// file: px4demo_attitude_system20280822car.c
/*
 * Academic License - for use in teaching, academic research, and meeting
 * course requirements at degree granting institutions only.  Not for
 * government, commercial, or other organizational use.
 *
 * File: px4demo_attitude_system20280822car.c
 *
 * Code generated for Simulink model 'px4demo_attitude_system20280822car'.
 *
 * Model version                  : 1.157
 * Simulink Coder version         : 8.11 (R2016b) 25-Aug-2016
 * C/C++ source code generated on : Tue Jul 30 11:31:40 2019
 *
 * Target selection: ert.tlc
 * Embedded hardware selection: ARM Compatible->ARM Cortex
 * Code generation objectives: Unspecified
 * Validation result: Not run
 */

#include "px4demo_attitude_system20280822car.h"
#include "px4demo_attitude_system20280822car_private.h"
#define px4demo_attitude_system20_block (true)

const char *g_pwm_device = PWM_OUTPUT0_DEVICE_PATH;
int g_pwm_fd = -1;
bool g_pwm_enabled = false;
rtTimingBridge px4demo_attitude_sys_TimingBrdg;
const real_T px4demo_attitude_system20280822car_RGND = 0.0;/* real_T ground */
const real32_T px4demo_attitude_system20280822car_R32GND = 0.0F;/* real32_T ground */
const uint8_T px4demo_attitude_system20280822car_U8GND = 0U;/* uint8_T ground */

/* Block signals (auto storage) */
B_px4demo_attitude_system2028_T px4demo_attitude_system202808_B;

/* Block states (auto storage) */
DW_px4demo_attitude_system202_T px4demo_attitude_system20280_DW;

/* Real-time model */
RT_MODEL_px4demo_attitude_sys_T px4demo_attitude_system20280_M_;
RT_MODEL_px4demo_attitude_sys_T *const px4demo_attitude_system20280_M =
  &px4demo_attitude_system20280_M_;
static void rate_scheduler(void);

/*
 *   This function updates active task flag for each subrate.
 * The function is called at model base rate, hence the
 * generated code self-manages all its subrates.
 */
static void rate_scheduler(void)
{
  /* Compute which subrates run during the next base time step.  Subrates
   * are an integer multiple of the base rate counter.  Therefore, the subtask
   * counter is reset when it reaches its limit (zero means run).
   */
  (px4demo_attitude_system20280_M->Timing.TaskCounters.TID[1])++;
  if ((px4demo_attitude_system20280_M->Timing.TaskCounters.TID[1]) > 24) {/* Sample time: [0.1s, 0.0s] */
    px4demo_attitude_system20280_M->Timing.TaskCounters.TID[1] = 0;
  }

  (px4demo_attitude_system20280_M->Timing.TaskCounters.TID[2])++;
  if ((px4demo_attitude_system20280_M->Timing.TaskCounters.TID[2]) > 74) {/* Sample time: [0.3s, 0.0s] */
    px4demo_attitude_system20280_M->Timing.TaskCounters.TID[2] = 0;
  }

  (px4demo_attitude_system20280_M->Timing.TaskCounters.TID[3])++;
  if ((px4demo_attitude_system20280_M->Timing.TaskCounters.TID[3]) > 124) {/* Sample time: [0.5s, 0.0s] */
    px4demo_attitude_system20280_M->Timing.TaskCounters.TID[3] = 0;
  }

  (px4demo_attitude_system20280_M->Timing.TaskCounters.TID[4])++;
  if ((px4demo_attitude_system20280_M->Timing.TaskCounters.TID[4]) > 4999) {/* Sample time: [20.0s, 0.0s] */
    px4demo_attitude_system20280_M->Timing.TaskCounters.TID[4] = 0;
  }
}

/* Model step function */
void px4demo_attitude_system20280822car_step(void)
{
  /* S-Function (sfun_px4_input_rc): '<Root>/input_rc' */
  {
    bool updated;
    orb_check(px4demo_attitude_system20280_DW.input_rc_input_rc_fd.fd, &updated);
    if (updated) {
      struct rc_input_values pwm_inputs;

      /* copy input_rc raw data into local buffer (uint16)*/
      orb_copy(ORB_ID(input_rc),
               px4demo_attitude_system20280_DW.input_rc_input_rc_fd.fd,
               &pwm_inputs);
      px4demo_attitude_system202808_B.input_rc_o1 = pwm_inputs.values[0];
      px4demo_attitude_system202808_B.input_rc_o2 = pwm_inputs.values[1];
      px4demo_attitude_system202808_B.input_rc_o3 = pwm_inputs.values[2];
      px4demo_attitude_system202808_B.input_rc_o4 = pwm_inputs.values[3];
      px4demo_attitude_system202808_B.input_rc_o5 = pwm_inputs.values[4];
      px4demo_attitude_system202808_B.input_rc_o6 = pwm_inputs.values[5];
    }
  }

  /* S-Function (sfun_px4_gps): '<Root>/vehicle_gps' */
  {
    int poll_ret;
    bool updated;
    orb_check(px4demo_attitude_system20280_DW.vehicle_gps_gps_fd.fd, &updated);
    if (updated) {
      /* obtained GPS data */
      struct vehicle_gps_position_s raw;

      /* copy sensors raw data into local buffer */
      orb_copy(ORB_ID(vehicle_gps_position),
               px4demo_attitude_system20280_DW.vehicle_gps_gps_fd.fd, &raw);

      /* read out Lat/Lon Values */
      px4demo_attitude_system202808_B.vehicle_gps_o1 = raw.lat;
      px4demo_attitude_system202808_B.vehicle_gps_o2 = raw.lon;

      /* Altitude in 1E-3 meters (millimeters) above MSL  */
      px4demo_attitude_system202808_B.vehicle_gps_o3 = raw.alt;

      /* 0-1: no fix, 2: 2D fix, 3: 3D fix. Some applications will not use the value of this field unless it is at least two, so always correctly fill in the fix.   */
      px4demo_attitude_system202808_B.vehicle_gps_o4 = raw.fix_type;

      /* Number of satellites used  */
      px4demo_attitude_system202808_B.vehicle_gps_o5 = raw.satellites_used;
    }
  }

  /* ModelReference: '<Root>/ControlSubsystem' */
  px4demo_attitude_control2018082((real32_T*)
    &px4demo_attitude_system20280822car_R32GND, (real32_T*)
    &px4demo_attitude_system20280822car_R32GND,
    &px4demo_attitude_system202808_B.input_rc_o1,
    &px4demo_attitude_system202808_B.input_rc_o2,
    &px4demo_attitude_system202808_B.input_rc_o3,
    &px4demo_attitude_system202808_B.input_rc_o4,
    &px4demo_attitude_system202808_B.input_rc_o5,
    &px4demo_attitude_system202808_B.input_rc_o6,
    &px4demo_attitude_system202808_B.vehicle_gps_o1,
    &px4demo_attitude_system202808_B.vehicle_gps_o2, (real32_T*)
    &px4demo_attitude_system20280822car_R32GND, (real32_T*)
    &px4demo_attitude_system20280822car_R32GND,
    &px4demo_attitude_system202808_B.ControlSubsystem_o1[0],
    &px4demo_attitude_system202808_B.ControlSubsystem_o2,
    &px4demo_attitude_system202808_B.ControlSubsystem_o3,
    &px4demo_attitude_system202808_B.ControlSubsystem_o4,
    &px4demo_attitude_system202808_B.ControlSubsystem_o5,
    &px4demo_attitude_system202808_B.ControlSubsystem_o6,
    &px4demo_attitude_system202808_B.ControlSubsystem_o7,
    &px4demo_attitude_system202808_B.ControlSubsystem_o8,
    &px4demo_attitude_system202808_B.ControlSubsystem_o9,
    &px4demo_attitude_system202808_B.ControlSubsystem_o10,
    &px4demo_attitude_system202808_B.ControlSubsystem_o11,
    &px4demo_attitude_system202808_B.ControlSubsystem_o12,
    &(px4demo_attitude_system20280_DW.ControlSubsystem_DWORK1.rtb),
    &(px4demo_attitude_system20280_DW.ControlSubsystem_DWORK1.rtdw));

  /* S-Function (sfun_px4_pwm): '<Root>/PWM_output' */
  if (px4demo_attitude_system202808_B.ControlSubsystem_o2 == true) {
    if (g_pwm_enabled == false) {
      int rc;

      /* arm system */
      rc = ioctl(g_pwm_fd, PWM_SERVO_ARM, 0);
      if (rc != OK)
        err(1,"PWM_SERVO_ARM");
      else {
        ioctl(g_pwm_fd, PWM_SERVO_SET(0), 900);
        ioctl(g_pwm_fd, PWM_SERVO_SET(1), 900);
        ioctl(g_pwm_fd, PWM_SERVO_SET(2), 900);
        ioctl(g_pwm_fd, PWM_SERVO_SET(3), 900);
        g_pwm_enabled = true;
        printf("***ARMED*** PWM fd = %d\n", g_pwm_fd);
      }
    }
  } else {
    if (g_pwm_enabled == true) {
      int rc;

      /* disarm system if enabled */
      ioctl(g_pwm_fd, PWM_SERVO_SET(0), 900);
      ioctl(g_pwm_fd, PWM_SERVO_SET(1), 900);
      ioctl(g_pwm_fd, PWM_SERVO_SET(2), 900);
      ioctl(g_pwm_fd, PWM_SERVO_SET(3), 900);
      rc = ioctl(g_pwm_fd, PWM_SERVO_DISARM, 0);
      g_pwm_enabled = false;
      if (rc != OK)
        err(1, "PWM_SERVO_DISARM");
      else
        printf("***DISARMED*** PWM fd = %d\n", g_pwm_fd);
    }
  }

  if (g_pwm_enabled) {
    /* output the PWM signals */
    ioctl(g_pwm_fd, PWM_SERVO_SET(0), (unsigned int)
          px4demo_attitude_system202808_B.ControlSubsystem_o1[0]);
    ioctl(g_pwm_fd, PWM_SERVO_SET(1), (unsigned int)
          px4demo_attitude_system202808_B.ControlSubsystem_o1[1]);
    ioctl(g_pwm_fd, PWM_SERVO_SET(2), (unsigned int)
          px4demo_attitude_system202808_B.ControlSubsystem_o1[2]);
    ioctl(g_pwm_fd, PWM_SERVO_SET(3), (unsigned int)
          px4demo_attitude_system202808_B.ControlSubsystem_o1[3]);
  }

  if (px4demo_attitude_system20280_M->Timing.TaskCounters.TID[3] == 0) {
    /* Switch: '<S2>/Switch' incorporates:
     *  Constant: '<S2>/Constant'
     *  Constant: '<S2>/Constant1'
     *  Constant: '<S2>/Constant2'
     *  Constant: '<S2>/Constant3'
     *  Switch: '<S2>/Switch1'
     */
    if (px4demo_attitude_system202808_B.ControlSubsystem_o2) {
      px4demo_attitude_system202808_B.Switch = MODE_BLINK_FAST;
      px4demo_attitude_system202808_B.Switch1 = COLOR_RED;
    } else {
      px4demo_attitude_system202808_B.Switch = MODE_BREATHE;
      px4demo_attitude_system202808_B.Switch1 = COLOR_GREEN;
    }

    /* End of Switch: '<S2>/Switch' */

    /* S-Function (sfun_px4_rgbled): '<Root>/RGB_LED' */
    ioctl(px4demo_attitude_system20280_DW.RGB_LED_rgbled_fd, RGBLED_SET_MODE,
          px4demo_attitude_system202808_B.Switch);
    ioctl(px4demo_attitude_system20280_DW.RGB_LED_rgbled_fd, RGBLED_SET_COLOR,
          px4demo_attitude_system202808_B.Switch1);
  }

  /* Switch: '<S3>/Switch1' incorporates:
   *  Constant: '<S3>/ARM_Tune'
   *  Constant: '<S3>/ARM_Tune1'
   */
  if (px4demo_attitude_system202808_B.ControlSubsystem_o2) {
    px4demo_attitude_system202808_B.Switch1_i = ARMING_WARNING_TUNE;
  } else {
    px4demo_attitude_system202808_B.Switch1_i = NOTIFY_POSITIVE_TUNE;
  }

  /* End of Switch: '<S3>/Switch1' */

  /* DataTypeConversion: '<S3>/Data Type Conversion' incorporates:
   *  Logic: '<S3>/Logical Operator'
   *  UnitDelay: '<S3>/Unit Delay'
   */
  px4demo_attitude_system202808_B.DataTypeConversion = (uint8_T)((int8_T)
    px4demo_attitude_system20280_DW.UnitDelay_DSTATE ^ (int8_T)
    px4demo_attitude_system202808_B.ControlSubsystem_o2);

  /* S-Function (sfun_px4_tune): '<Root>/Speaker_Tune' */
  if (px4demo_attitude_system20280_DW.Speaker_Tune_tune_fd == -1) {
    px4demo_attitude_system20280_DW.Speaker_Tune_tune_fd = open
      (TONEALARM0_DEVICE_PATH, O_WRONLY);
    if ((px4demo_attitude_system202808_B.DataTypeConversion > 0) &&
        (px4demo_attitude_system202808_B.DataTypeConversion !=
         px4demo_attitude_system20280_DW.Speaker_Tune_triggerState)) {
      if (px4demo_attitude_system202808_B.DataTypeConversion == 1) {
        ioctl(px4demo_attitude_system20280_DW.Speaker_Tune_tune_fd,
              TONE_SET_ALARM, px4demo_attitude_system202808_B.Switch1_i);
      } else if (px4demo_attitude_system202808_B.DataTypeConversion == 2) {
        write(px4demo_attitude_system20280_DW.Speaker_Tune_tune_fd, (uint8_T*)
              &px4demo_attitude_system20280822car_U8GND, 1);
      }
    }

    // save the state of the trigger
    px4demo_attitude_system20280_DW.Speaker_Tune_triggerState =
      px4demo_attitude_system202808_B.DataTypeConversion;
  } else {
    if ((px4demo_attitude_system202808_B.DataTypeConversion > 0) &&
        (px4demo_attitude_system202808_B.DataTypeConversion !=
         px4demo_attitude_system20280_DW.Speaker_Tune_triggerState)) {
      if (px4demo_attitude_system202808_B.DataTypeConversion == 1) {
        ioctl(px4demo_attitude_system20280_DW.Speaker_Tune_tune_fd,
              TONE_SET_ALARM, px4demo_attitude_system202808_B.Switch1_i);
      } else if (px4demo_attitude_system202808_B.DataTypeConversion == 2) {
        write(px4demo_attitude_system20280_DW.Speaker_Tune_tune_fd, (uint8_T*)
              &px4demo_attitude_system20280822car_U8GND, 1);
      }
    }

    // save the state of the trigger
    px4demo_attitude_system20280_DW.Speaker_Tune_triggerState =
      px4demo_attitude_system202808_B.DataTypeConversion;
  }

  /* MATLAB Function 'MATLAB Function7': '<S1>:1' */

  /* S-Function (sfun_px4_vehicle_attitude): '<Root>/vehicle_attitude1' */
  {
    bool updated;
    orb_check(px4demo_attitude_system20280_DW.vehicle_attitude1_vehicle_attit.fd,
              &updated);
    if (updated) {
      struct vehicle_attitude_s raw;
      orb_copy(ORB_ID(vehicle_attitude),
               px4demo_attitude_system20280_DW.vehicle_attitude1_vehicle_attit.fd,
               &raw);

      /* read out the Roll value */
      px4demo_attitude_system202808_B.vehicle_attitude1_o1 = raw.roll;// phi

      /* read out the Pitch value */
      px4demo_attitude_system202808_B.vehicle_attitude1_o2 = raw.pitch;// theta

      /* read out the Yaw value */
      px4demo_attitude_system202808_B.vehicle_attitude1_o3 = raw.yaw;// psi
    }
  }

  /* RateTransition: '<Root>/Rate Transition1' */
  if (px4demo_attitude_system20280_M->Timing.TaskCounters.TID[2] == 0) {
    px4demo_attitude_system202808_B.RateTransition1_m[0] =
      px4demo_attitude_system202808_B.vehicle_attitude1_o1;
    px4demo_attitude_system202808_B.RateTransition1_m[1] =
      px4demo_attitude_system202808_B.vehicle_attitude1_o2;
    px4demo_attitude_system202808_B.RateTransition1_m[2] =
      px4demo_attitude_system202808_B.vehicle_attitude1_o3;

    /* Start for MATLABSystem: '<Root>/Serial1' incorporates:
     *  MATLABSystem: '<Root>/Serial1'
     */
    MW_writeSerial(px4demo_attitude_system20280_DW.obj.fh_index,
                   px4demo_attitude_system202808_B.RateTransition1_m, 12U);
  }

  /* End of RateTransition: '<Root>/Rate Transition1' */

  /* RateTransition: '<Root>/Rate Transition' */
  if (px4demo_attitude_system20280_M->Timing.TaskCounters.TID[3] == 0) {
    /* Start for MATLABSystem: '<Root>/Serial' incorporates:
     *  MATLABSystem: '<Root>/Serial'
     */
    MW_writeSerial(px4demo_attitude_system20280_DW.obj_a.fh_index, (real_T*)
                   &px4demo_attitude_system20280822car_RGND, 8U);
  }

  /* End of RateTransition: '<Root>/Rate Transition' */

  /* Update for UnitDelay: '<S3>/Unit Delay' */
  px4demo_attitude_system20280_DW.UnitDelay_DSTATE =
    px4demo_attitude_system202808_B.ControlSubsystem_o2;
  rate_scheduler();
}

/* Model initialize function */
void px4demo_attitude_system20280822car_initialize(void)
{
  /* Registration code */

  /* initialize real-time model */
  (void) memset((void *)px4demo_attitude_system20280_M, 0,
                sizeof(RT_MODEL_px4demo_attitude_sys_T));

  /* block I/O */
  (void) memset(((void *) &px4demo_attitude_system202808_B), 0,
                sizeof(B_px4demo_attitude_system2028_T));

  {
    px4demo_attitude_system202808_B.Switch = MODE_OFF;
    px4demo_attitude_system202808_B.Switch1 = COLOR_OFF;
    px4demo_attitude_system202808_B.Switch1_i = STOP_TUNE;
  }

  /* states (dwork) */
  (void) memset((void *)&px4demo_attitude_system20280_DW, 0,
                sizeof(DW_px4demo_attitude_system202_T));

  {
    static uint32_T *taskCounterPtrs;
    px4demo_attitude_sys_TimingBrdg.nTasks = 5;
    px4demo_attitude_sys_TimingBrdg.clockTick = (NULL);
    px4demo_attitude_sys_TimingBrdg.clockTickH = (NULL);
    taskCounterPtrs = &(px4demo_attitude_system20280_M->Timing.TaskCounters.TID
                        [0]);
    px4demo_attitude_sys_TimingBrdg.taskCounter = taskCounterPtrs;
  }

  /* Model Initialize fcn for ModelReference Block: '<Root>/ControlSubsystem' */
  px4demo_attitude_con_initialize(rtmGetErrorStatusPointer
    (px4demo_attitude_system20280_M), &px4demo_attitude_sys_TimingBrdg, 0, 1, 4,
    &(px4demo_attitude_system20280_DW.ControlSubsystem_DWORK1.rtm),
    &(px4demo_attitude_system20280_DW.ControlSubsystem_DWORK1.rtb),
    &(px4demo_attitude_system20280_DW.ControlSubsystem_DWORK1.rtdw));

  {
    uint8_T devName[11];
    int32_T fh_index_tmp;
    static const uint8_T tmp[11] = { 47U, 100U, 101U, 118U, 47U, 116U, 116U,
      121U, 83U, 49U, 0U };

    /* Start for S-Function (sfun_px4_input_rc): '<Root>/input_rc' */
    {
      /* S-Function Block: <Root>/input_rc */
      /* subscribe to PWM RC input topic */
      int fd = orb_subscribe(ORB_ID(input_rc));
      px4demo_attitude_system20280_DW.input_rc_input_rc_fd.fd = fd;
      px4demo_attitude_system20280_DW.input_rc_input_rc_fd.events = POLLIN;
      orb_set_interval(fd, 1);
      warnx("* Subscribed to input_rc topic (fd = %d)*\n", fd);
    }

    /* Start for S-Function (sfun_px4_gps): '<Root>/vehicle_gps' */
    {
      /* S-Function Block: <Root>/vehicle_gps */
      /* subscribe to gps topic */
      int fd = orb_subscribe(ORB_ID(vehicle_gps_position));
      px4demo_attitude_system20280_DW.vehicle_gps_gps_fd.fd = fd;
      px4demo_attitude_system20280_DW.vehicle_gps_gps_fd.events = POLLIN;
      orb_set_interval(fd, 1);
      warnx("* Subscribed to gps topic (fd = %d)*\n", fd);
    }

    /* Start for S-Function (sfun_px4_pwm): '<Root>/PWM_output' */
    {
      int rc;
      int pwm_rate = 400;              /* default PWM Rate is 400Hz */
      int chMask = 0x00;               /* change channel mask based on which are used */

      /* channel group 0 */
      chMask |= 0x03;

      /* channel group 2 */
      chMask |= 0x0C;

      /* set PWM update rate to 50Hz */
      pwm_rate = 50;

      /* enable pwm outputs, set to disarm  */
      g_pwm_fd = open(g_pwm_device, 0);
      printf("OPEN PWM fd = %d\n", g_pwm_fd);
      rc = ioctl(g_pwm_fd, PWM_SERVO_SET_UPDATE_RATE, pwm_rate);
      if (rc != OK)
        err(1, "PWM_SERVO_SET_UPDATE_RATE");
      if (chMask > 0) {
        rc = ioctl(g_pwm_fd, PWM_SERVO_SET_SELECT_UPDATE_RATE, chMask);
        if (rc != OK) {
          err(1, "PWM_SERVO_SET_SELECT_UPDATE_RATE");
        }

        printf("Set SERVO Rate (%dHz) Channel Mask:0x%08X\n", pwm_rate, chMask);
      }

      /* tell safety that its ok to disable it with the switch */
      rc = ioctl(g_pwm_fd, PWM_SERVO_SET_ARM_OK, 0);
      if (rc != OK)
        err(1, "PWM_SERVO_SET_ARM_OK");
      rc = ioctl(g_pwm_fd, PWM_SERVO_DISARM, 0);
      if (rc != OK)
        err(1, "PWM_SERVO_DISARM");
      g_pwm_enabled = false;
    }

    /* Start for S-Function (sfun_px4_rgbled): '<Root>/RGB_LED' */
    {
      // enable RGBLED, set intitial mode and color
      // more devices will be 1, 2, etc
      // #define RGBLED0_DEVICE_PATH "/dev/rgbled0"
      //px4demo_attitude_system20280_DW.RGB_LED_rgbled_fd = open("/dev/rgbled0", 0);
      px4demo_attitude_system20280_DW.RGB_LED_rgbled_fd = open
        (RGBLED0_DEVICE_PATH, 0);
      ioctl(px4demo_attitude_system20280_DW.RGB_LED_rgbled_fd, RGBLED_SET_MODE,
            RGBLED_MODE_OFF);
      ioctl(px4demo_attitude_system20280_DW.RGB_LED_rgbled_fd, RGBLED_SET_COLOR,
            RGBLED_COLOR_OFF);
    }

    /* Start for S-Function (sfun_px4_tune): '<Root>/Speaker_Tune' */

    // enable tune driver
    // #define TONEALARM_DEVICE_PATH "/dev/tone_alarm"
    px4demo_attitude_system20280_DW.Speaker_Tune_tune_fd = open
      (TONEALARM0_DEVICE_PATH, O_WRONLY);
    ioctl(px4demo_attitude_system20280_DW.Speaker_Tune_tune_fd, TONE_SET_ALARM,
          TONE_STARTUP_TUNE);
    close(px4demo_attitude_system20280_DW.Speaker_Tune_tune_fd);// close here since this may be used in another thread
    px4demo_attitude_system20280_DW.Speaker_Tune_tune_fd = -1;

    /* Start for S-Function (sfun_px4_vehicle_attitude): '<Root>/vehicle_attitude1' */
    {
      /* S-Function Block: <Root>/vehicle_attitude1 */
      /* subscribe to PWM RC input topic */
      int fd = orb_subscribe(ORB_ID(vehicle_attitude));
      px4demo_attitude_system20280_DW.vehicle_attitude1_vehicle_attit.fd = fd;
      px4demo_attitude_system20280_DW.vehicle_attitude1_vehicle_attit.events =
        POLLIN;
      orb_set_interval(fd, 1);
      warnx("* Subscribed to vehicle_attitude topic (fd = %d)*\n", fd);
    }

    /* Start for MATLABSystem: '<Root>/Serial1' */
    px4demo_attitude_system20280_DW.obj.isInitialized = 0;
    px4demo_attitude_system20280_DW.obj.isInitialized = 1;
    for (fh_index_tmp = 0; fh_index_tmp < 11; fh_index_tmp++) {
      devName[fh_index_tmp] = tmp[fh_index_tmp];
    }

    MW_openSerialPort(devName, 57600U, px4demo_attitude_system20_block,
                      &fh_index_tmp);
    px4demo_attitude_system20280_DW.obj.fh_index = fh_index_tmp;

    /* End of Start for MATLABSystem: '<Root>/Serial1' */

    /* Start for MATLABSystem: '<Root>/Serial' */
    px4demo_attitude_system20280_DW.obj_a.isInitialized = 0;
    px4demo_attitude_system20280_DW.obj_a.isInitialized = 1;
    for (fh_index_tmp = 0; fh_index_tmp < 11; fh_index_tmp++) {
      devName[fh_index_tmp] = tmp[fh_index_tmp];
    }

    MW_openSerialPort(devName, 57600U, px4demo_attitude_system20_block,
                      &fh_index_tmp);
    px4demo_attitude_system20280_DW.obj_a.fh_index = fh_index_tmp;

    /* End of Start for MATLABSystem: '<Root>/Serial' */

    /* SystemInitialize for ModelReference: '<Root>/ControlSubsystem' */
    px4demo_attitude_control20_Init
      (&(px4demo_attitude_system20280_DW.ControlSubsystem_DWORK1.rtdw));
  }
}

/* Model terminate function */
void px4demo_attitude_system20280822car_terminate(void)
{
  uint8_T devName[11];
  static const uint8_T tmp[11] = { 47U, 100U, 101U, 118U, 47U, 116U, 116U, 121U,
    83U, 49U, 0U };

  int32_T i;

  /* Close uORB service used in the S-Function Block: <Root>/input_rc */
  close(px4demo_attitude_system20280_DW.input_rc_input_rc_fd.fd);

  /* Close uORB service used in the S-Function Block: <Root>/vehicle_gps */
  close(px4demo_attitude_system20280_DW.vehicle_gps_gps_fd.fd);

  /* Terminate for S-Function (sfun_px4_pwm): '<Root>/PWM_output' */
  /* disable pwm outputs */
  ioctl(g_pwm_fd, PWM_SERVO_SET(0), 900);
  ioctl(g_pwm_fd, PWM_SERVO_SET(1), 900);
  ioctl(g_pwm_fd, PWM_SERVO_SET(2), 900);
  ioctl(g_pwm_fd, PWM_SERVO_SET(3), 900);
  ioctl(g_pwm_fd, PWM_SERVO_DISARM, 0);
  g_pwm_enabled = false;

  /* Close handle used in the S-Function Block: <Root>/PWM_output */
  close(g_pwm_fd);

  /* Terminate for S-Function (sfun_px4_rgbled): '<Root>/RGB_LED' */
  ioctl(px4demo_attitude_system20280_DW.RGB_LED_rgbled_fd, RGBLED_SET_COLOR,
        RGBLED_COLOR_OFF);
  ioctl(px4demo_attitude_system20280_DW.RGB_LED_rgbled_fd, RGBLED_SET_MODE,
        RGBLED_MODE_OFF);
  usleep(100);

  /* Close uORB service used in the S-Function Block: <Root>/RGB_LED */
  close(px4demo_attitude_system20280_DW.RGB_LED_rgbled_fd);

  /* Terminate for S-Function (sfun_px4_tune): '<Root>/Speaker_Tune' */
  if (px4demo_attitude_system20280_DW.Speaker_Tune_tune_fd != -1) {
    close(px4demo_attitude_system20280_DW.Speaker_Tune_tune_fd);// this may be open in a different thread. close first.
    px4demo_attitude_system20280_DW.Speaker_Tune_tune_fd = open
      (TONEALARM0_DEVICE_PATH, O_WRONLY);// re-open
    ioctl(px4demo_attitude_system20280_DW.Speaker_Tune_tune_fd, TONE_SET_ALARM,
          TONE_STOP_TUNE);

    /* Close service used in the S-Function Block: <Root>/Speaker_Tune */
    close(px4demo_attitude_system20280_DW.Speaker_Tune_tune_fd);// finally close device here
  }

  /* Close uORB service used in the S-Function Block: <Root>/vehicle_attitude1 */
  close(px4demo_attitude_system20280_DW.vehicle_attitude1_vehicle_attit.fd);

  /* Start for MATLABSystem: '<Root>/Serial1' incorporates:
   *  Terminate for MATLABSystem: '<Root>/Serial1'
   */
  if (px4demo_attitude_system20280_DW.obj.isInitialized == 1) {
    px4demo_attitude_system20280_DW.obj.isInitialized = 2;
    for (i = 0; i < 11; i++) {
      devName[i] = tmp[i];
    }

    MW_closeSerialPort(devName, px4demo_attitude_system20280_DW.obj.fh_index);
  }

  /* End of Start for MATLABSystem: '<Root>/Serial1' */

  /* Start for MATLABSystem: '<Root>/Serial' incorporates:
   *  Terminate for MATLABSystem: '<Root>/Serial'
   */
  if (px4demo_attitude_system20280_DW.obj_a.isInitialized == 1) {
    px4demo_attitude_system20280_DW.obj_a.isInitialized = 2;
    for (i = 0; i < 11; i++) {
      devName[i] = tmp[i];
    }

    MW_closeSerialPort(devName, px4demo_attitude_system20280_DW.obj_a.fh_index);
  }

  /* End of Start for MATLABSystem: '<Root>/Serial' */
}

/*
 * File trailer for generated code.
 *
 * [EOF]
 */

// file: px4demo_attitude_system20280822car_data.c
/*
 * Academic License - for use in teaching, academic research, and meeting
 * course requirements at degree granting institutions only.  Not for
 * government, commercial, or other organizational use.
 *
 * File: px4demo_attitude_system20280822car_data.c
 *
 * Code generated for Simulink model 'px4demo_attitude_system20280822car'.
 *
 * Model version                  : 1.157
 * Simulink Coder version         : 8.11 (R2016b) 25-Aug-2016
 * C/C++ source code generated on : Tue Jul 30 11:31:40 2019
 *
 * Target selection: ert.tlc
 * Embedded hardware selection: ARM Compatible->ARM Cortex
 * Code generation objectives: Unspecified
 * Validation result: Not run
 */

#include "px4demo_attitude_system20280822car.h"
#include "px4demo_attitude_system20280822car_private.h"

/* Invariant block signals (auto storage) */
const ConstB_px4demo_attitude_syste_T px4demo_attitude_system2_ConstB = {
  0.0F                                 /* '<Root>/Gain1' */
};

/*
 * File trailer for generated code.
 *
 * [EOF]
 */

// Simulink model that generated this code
simulink model "px4demo_attitude_system20280822car"  (R2016b)
settings: Solver=FixedStepDiscrete  StartTime=0.0  StopTime=inf  RelTol=1e-3
PostLoadFcn:
  | kFactor = 1.2;
  | 
  | KpRollAttitude = 0.630138625117681 / kFactor;
  | KiRollAttitude = 0.0552303199591522 / kFactor;
  | 
  | KpPitchAttitude = 0.630138625117681 / kFactor;
  | KiPitchAttitude = 0.0552303199591522 / kFactor;
  | 
  | KpRollRate = 1.31533836563383 / kFactor;
  | KiRollRate = 0.460338699849681 / kFactor;
  | 
  | KpPitchRate = 1.31533836563383 / kFactor;
  | KiPitchRate = 0.460338699849681 / kFactor;
  | 
  | KpYawRate = 1.31533836563383 / kFactor;
  | KiYawRate = 0.460338699849681 / kFactor;
undefined symbols (not defined in the file or in its folder): PX4_TUNE_ENUM, RGBLED_COLOR_ENUM, RGBLED_MODE_ENUM
libraries: pixhawk_slib_sensors_actuators x7, pixhawk_slib_ADC_serial x2

== system px4demo_attitude_system20280822car ==
  note: PX4 PSP Demo - Attitude Control System
  note: Copyright 2015- 2016 The MathWorks, Inc.
  ControlSubsystem : ModelReference  ModelNameDialog=px4demo_attitude_control20180822car.slx  SimulationMode=Normal  ModelReferenceVersion=1.380
  Data Type Conversion{1..5,10..12} (8 alike) : DataTypeConversion  OutDataTypeStr=single
  Demux9 : Demux
  Gain1 : Gain  Gain=180/pi
  MATLAB Function7 : MATLAB Function  TreatAsAtomicUnit=on
  Mux1 : Mux  Inputs=3
  Mux2 : Mux  Inputs=8
  PWM_output : pixhawk_slib_sensors_actuators/PWM_output  pwm_rate=50Hz  show_pwm1=on  show_pwm2=on  show_pwm3=on  show_pwm4=on  show_pwm5=off  show_pwm6=off  show_pwm7=off  show_pwm8=off
  RGB_LED : pixhawk_slib_sensors_actuators/RGB_LED
  RGB_Mode_Subsystem : Subsystem
  Rate Transition : RateTransition  OutPortSampleTime=0.5
  Rate Transition1 : RateTransition  OutPortSampleTime=0.5
  Serial : pixhawk_slib_ADC_serial/Serial  DeviceName=/dev/ttyS1  ReadOrWrite=Writing  BaudRateStr=57600  block=on  WriteStatus=on  Terminator=off  Header=off  NumBytesRead=4  TerminatorChar=\n  HeaderData=57600  SimulateUsing=Code generation
  Serial1 : pixhawk_slib_ADC_serial/Serial  DeviceName=/dev/ttyS1  ReadOrWrite=Writing  BaudRateStr=57600  block=off  WriteStatus=on  Terminator=off  Header=off  NumBytesRead=4  TerminatorChar=\n  HeaderData=57600  SimulateUsing=Code generation
  Speaker_Tune : pixhawk_slib_sensors_actuators/Speaker_Tune
  Tune_Mode_Subsystem : Subsystem
  input_rc : pixhawk_slib_sensors_actuators/input_rc  sampletime=1/250  channel1=on  channel2=on  channel3=on  channel4=on  channel5=on  channel6=on  channel7=off  channel8=off  ch_count=off  rssi=off  rc_failsafe=off  rc_lost=off  rc_inputsource=off
  vehicle_attitude : pixhawk_slib_sensors_actuators/vehicle_attitude  sampletime=1/250  show_r=on  show_p=on  show_y=on  show_q=off
  vehicle_attitude1 : pixhawk_slib_sensors_actuators/vehicle_attitude  sampletime=1/250  show_r=on  show_p=on  show_y=on  show_q=off
  vehicle_gps : pixhawk_slib_sensors_actuators/vehicle_gps  sampletime=1/250  show_ts_pos=off  show_alt=on  show_ts_gps=off  show_vel=off  show_fixtype=on  show_numsat=on
  wires:
  Demux9/4 -> PWM_output/5
  Demux9/2 -> PWM_output/3
  Demux9/3 -> PWM_output/4
  Demux9/1 -> PWM_output/2
  RGB_Mode_Subsystem/1(RGB_MODE) -> RGB_LED/1
  RGB_Mode_Subsystem/2(RGB_COLOR) -> RGB_LED/2
  Tune_Mode_Subsystem/1(TUNE) -> Speaker_Tune/1
  Tune_Mode_Subsystem/2(GND) -> Speaker_Tune/2
  Tune_Mode_Subsystem/3(TRIGGER) -> Speaker_Tune/3
  ControlSubsystem/2 -> Tune_Mode_Subsystem/1(ARM_STATE), PWM_output/1, RGB_Mode_Subsystem/1(ARM_STATE)
  vehicle_attitude/1 -> ControlSubsystem/1  "phi"
  vehicle_attitude/2 -> ControlSubsystem/2  "theta"
  input_rc/1 -> ControlSubsystem/3
  input_rc/2 -> ControlSubsystem/4
  input_rc/3 -> ControlSubsystem/5
  input_rc/4 -> ControlSubsystem/6
  input_rc/5 -> ControlSubsystem/7
  ControlSubsystem/1 -> Demux9/1
  input_rc/6 -> ControlSubsystem/8
  Rate Transition/1 -> Serial/1
  Mux2/1 -> Rate Transition/1
  vehicle_gps/1 -> ControlSubsystem/9
  vehicle_gps/2 -> ControlSubsystem/10
  ControlSubsystem/4 -> Data Type Conversion11/1
  ControlSubsystem/3 -> Data Type Conversion10/1
  Data Type Conversion12/1 -> Gain1/1
  vehicle_attitude/3 -> ControlSubsystem/11, Data Type Conversion12/1
  Gain1/1 -> MATLAB Function7/1(u)
  ControlSubsystem/5 -> Data Type Conversion1/1
  Data Type Conversion1/1 -> Mux2/1
  Data Type Conversion10/1 -> Mux2/2
  Data Type Conversion11/1 -> Mux2/3
  MATLAB Function7/1(y) -> Mux2/4
  ControlSubsystem/6 -> Data Type Conversion3/1
  Data Type Conversion3/1 -> Mux2/5
  ControlSubsystem/7 -> Data Type Conversion2/1
  Data Type Conversion2/1 -> Mux2/6
  ControlSubsystem/8 -> Data Type Conversion4/1
  ControlSubsystem/9 -> Data Type Conversion5/1
  Data Type Conversion4/1 -> Mux2/7
  Data Type Conversion5/1 -> Mux2/8
  Rate Transition1/1 -> Serial1/1
  vehicle_attitude1/1 -> Mux1/1
  vehicle_attitude1/2 -> Mux1/2
  vehicle_attitude1/3 -> Mux1/3
  Mux1/1 -> Rate Transition1/1

== system px4demo_attitude_system20280822car/RGB_Mode_Subsystem ==
  ARM_STATE : Inport
  Constant : Constant  Value=RGBLED_MODE_ENUM.MODE_BLINK_FAST  OutDataTypeStr=Enum: RGBLED_MODE_ENUM
  Constant1 : Constant  Value=RGBLED_MODE_ENUM.MODE_BREATHE  OutDataTypeStr=Enum: RGBLED_MODE_ENUM
  Constant2 : Constant  Value=RGBLED_COLOR_ENUM.COLOR_GREEN  OutDataTypeStr=Enum: RGBLED_COLOR_ENUM
  Constant3 : Constant  Value=RGBLED_COLOR_ENUM.COLOR_RED  OutDataTypeStr=Enum: RGBLED_COLOR_ENUM
  Switch : Switch  Criteria=u2 ~= 0  Threshold=1500  SampleTime=1/2
  Switch1 : Switch  Criteria=u2 ~= 0  Threshold=1500  SampleTime=1/2
  RGB_MODE : Outport
  RGB_COLOR : Outport  Port=2
  wires:
  ARM_STATE/1 -> Switch1/2, Switch/2
  Constant/1 -> Switch/1
  Constant1/1 -> Switch/3
  Switch/1 -> RGB_MODE/1
  Constant3/1 -> Switch1/1
  Constant2/1 -> Switch1/3
  Switch1/1 -> RGB_COLOR/1

== system px4demo_attitude_system20280822car/Tune_Mode_Subsystem ==
  ARM_STATE : Inport
  ARM_Tune : Constant  Value=PX4_TUNE_ENUM.ARMING_WARNING_TUNE  OutDataTypeStr=Enum: PX4_TUNE_ENUM
  ARM_Tune1 : Constant  Value=PX4_TUNE_ENUM.NOTIFY_POSITIVE_TUNE  OutDataTypeStr=Enum: PX4_TUNE_ENUM
  Data Type Conversion : DataTypeConversion  OutDataTypeStr=uint8
  Ground : Ground
  Logical Operator : Logic  Operator=XOR  IconShape=distinctive  AllPortsSameDT=off  OutDataTypeStr=boolean
  Switch1 : Switch  Criteria=u2 ~= 0  Threshold=1500
  Unit Delay : UnitDelay  SampleTime=-1
  TUNE : Outport
  GND : Outport  Port=2
  TRIGGER : Outport  Port=3
  wires:
  Ground/1 -> GND/1
  Data Type Conversion/1 -> TRIGGER/1
  Switch1/1 -> TUNE/1
  ARM_Tune/1 -> Switch1/1
  ARM_Tune1/1 -> Switch1/3
  ARM_STATE/1 -> Logical Operator/2, Unit Delay/1, Switch1/2
  Unit Delay/1 -> Logical Operator/1
  Logical Operator/1 -> Data Type Conversion/1

== matlab function px4demo_attitude_system20280822car/MATLAB Function7 ==
function y = fcn(u)
if(u<=0)
    y=360+u;
else
    y=u
end
